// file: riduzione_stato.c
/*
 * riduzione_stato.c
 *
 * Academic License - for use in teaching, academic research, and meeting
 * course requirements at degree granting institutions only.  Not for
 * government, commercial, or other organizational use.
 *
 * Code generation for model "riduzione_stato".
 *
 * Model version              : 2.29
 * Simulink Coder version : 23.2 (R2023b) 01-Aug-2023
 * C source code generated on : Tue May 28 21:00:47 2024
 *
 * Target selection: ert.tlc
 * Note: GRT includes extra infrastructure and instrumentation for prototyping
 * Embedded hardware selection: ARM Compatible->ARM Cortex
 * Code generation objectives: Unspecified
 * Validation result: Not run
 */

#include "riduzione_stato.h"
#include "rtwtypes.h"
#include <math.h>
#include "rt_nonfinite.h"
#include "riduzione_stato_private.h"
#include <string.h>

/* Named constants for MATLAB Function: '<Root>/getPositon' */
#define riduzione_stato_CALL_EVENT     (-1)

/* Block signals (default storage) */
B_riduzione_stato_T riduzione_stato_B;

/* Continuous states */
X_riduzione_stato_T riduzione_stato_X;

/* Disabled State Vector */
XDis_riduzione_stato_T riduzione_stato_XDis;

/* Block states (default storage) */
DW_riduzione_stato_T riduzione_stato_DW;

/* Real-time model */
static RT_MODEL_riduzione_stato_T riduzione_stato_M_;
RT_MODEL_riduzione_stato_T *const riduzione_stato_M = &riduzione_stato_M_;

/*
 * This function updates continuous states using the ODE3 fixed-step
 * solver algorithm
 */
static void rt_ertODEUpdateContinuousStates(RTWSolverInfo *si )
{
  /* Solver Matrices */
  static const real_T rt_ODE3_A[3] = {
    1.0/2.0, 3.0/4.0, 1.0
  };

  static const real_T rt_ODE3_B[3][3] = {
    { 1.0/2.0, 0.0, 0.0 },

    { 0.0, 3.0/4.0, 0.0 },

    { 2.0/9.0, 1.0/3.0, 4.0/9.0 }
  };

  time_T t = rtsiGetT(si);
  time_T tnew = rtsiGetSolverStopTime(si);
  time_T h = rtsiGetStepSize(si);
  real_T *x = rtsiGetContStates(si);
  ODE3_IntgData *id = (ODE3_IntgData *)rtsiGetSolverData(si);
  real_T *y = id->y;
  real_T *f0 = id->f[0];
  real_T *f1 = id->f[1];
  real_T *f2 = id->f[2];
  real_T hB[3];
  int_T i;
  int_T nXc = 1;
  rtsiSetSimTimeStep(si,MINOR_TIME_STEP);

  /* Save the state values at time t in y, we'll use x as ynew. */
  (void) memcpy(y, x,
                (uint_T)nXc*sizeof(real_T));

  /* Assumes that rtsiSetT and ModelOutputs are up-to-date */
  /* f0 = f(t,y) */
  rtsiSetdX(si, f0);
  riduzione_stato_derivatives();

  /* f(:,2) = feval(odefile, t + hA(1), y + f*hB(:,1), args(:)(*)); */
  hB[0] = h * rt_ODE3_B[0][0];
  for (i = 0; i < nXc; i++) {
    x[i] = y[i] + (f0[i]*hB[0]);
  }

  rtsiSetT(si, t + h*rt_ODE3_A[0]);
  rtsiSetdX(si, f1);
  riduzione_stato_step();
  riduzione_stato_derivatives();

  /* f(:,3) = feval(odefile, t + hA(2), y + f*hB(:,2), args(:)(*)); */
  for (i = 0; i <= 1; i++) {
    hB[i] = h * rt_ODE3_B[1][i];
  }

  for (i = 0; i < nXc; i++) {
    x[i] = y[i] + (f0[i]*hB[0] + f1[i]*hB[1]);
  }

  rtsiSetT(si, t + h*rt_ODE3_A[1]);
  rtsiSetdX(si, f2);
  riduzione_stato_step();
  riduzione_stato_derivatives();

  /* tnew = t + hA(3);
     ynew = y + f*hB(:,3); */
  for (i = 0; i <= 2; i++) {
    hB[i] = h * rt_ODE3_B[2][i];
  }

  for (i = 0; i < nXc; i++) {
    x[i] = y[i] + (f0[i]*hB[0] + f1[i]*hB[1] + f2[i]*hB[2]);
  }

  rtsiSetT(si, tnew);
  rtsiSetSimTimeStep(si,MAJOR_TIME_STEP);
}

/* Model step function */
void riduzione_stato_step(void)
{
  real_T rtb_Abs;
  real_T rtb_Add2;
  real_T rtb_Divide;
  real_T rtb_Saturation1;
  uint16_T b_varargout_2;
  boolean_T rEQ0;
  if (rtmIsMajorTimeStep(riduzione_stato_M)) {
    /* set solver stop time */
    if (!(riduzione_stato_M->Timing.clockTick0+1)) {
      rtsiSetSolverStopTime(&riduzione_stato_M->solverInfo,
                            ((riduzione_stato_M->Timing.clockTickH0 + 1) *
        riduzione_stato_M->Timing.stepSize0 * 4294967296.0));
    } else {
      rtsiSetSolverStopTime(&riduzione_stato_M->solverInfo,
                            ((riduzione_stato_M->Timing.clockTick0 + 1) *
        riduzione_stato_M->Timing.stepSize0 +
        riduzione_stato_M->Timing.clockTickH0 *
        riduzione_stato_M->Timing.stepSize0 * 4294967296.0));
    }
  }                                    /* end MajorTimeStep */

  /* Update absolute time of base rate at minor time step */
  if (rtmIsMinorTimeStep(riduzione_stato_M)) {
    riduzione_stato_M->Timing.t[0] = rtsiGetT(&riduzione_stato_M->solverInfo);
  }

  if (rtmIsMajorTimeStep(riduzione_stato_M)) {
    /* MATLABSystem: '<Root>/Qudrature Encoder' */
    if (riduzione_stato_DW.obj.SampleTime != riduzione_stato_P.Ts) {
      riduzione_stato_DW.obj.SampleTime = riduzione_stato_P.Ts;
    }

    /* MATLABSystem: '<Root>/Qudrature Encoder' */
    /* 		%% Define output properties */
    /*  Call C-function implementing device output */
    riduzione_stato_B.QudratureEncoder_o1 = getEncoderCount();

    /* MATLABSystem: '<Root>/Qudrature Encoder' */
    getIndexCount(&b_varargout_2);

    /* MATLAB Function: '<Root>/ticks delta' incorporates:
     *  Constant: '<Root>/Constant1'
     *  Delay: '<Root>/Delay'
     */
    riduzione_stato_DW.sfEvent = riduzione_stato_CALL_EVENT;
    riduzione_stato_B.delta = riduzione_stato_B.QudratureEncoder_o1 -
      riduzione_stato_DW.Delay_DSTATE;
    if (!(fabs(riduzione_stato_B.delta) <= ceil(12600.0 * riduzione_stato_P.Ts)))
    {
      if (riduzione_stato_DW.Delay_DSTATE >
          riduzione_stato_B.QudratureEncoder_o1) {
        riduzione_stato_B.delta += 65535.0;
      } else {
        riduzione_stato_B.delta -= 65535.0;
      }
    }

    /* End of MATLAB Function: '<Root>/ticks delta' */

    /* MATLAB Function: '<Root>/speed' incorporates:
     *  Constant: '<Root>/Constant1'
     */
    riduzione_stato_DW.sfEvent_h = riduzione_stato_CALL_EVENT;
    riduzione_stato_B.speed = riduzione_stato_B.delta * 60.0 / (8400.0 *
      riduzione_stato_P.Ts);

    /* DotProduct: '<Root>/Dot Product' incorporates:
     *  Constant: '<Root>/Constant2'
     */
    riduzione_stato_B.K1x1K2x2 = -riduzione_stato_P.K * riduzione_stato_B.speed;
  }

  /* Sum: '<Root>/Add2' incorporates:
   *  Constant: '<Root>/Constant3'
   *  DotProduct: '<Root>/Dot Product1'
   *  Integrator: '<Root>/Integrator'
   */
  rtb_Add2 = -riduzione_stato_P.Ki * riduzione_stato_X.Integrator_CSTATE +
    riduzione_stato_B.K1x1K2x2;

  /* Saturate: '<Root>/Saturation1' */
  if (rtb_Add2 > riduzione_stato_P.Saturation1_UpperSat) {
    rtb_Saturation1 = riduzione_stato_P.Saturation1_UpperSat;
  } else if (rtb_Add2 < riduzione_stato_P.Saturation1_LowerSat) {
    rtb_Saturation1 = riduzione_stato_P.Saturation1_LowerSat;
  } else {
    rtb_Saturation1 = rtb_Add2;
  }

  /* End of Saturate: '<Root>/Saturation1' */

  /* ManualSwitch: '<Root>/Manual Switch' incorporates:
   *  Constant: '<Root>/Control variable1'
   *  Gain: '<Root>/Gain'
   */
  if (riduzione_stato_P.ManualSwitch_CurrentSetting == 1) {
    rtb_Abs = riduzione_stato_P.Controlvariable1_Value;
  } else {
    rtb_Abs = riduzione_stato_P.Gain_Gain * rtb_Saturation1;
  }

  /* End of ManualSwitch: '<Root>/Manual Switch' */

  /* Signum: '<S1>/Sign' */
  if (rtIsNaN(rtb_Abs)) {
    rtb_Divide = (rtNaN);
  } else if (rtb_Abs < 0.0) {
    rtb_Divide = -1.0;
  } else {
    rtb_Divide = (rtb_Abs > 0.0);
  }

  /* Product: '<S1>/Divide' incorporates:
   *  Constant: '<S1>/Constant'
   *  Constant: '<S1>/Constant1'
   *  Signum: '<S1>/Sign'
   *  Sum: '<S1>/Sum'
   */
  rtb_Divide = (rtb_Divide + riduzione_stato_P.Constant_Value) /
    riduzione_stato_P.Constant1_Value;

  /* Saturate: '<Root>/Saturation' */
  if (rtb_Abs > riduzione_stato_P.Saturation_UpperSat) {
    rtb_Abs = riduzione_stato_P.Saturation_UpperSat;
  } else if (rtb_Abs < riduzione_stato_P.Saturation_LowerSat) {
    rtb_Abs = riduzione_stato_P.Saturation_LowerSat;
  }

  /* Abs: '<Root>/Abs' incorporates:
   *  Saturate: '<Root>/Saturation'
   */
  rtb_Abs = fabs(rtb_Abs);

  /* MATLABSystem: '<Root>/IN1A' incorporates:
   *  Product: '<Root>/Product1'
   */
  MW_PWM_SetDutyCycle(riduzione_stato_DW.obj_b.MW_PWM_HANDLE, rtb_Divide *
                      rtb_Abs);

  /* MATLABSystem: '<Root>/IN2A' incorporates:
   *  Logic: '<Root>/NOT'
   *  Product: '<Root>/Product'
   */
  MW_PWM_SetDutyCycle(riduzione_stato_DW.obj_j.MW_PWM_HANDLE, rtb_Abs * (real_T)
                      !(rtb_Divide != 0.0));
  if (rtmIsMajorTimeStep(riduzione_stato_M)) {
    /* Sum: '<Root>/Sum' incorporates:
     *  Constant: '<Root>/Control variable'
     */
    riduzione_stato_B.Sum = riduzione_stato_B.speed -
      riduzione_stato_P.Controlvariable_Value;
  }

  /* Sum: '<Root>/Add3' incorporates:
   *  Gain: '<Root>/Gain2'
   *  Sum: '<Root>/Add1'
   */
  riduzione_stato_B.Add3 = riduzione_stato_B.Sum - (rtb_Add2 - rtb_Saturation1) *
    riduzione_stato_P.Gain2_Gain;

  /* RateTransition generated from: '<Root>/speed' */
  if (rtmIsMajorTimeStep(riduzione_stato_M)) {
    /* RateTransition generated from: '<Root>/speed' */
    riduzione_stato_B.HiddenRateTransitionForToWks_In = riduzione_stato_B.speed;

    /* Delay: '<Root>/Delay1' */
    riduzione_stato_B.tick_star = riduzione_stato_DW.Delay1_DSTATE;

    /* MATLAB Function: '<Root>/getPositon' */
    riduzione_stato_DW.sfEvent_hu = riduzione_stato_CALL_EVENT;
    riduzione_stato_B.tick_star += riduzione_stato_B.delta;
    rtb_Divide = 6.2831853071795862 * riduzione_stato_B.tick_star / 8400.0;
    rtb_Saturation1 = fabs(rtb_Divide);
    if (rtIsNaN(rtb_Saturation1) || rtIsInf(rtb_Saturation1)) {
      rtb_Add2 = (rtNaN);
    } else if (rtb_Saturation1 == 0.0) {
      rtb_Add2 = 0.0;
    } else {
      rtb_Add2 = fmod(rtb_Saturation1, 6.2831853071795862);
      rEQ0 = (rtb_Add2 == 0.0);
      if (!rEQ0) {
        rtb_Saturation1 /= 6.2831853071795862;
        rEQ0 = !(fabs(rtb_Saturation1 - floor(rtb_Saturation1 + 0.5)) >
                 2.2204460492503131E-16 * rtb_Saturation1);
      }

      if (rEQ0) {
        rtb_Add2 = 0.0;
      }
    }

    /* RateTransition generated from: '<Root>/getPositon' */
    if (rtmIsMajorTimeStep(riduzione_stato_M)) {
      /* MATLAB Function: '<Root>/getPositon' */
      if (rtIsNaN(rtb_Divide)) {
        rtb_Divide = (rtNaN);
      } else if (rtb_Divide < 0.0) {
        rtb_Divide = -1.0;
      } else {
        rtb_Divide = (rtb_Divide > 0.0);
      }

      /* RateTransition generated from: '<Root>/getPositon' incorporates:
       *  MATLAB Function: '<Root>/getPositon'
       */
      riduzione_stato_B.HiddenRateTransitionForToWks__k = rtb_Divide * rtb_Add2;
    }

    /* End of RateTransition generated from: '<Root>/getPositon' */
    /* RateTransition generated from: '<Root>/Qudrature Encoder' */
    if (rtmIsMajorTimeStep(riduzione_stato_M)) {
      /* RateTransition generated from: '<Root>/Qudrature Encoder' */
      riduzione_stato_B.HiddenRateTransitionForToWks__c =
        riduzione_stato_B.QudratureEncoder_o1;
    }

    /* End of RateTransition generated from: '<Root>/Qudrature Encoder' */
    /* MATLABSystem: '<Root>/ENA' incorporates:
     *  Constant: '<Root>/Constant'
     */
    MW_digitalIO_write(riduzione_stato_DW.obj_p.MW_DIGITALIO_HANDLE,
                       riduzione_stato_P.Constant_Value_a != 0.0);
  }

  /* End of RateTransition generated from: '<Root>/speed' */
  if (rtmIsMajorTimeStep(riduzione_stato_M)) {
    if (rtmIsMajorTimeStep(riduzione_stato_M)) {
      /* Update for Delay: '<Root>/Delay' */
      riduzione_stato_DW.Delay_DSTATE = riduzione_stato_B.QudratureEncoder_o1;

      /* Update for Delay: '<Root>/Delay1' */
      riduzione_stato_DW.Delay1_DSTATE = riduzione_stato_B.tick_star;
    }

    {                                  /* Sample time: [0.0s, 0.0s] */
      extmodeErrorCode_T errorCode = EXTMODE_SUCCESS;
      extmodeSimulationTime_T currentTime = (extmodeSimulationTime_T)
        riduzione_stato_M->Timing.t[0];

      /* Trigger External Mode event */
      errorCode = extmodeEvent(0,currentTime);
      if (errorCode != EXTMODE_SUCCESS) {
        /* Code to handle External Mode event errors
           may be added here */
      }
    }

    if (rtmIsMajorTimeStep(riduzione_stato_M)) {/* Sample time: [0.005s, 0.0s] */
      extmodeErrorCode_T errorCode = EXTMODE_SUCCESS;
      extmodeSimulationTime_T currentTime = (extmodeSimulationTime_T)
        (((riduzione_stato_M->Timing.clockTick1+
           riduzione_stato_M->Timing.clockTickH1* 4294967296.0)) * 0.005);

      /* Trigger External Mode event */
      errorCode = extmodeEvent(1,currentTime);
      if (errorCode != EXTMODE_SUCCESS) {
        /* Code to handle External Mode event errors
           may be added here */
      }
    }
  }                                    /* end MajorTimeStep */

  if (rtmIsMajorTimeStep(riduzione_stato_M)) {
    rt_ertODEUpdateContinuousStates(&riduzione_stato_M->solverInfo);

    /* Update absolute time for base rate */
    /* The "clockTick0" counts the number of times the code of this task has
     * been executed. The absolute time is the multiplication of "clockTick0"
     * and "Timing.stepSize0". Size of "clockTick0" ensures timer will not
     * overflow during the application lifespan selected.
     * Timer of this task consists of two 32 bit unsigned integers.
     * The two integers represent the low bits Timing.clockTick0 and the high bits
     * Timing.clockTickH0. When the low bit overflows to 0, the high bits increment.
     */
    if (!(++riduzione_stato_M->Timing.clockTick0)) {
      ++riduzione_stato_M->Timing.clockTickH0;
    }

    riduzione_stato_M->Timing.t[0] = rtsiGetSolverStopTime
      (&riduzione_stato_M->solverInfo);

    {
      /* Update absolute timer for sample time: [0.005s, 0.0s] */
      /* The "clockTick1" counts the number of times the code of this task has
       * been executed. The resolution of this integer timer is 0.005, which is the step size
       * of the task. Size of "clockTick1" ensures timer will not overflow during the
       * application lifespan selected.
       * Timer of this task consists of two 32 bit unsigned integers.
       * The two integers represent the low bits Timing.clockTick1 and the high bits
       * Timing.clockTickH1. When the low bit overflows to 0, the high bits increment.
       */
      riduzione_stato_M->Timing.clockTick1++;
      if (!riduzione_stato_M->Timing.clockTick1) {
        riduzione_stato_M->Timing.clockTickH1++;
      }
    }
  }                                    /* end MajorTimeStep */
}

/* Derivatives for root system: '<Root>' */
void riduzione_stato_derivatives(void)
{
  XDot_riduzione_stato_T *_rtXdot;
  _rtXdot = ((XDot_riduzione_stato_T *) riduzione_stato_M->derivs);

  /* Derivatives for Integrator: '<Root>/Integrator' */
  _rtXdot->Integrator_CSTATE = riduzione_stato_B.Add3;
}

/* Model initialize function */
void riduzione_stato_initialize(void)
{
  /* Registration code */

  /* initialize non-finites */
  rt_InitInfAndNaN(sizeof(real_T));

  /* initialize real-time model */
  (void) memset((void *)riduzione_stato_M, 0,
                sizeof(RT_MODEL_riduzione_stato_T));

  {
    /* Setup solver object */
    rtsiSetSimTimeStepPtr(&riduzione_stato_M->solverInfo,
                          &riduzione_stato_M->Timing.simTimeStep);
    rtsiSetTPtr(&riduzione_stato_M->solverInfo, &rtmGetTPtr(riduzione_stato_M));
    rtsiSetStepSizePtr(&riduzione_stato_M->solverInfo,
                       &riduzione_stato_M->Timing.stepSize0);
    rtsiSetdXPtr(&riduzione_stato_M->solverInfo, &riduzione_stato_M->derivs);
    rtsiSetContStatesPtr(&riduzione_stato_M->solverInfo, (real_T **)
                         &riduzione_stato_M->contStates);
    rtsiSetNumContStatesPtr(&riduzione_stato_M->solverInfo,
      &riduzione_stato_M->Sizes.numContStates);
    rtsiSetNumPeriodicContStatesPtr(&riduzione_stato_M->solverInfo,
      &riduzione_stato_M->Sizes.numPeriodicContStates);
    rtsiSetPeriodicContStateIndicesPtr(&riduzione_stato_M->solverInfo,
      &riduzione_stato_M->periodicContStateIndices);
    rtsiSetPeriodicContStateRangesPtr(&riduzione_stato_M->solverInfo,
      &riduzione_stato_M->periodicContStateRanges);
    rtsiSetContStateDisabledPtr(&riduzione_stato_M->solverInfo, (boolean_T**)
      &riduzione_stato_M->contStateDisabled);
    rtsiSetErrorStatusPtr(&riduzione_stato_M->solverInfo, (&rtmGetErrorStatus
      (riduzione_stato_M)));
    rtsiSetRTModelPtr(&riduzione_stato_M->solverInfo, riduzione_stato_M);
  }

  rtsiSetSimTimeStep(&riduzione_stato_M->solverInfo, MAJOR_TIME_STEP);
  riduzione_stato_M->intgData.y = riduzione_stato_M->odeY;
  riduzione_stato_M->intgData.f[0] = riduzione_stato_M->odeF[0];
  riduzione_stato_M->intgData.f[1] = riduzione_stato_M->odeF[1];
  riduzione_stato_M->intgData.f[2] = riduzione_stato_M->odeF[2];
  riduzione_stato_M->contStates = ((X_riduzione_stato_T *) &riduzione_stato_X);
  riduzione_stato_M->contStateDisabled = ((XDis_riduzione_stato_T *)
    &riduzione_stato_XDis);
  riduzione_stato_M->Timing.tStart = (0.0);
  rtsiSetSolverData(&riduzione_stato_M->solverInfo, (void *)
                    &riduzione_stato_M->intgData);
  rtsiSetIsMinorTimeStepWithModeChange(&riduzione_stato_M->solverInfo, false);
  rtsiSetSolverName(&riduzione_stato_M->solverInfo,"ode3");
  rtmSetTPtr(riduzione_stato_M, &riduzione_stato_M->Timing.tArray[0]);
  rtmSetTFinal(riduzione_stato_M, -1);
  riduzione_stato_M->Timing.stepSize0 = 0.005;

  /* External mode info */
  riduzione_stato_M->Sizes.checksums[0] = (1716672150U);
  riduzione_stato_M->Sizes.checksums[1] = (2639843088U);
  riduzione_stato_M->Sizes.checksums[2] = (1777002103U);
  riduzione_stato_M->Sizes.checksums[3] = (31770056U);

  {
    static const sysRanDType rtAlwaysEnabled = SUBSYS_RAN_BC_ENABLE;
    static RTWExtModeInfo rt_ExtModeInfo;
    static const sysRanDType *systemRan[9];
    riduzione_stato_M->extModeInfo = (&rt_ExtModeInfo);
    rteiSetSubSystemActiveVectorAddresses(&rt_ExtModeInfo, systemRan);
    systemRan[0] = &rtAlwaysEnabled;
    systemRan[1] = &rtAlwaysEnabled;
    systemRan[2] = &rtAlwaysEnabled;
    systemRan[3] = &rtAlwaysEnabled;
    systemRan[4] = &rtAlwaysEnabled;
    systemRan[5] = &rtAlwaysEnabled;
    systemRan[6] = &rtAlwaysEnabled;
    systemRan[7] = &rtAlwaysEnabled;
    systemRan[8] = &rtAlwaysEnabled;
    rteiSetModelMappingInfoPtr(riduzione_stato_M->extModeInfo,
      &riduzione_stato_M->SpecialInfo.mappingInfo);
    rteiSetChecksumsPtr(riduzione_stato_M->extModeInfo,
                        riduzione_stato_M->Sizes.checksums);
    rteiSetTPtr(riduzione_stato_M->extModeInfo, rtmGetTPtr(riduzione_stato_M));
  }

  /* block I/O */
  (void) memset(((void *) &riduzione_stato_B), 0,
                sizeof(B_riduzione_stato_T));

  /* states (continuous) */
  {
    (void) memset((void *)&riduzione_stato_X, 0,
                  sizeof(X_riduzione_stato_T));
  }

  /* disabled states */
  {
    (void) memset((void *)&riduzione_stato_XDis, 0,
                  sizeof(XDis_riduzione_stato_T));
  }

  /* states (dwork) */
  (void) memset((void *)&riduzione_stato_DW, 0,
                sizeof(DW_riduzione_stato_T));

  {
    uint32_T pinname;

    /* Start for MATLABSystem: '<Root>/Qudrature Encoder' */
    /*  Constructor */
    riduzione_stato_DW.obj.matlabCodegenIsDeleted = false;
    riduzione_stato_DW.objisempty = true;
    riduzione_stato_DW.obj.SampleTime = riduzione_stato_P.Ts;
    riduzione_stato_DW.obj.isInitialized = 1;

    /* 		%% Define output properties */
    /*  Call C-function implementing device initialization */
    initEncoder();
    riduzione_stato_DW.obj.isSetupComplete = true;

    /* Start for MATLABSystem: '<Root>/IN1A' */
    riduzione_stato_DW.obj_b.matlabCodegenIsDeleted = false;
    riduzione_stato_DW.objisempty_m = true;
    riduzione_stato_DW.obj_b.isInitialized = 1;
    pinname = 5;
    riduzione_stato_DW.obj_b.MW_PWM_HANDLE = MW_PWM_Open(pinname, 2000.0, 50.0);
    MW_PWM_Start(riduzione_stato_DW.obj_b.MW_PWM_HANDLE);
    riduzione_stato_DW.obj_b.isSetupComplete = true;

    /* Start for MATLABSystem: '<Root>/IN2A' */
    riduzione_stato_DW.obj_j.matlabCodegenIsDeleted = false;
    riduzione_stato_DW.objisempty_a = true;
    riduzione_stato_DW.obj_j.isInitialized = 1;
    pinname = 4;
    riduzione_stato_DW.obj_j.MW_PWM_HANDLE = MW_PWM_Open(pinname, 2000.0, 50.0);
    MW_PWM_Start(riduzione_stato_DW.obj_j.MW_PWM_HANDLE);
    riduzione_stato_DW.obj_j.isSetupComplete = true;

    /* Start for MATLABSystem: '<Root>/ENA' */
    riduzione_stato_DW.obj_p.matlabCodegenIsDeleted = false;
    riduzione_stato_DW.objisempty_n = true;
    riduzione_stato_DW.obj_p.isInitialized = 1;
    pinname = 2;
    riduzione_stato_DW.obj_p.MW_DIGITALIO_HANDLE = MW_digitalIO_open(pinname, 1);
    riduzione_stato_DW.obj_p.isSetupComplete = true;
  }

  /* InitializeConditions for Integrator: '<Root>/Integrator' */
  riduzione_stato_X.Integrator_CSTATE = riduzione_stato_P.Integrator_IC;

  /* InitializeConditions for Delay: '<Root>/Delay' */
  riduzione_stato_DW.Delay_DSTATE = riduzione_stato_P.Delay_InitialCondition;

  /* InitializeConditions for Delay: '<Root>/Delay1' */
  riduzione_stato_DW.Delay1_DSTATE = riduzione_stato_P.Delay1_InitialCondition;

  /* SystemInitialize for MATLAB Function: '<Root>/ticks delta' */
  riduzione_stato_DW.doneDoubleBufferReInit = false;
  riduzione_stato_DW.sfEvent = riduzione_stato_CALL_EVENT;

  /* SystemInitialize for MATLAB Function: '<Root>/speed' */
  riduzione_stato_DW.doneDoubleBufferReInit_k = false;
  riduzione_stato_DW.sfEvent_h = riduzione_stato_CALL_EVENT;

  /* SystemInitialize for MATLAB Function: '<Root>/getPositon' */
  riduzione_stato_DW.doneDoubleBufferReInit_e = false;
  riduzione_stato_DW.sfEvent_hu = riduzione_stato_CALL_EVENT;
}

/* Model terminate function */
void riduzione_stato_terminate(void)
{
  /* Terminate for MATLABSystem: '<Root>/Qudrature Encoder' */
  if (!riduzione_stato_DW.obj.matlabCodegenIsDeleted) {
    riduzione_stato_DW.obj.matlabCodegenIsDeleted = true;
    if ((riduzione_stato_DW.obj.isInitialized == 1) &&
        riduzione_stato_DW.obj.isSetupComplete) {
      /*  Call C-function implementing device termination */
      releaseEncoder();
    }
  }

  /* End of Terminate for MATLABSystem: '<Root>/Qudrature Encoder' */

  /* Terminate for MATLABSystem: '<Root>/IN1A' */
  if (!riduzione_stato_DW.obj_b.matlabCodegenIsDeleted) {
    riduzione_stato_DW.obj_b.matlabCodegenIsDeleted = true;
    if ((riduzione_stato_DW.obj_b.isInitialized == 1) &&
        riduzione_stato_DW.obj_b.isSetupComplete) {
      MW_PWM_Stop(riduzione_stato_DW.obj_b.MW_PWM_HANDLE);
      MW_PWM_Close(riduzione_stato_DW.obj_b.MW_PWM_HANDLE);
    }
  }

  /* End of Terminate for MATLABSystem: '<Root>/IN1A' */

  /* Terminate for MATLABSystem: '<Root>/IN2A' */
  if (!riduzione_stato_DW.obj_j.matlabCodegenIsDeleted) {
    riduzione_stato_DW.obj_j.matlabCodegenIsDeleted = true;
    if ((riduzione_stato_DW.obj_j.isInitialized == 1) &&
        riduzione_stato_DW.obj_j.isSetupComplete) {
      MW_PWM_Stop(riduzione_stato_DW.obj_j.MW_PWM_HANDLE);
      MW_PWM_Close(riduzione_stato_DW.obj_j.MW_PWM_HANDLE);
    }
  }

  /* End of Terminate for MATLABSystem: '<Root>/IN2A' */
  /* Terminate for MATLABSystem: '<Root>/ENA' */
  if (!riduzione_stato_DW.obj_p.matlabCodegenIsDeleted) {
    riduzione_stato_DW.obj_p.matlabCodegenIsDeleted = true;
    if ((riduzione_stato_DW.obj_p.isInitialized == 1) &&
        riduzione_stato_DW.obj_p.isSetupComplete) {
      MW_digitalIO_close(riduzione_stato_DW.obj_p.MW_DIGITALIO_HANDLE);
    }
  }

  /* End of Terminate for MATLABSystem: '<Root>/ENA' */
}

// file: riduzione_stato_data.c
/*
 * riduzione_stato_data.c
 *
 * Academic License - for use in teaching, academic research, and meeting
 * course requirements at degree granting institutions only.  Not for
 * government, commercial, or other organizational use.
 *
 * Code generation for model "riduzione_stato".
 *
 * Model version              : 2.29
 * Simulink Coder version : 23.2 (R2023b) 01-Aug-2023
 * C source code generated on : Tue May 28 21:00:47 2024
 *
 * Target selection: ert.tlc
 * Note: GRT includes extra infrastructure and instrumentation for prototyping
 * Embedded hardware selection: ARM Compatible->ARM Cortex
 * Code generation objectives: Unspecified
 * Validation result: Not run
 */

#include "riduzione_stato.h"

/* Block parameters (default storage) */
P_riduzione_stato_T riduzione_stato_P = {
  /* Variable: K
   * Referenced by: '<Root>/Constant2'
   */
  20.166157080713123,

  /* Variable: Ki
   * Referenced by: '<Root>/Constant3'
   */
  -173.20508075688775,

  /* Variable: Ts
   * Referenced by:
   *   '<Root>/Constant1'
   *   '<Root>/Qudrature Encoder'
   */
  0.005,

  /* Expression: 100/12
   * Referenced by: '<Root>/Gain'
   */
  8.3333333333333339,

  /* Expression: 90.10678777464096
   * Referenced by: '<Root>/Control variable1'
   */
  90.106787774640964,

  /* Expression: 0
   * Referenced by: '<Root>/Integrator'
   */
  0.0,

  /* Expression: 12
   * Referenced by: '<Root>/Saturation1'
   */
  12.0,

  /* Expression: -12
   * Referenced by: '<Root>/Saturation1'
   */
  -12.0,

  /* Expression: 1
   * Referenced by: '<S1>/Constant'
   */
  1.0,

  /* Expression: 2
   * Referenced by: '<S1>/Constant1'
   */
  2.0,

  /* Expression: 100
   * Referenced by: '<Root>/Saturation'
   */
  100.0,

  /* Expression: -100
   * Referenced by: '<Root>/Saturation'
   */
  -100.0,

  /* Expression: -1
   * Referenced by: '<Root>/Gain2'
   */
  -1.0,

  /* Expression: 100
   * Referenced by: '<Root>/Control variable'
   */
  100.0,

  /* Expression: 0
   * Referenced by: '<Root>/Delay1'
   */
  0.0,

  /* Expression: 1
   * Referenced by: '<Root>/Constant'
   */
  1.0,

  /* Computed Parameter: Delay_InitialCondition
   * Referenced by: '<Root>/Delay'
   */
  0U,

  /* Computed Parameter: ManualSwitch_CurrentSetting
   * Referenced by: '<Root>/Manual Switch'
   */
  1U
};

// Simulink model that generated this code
simulink model "riduzione_stato"  (R2023b)
settings: Solver=FixedStepAuto  StartTime=0.0  StopTime=inf  RelTol=1e-3  EnableMultiTasking=on
undefined symbols (not defined in the file): K, Ki, Ts
libraries: mbedblockslib x3, stm_qeplib x1

== system riduzione_stato ==
  Abs : Abs  SaturateOnIntegerOverflow=off
  Add1 : Sum  Inputs=-+
  Add2 : Sum
  Add3 : Sum  Inputs=-+
  Constant : Constant
  Constant1 : Constant  Value=Ts
  Constant2 : Constant  Value=-K
  Constant3 : Constant  Value=-Ki
  Control variable : Constant  Value=-100
  Control variable1 : Constant  Value=100
  Delay : Delay  DelayLength=1
  Delay1 : Delay  DelayLength=1  InitialCondition=0
  Dot Product : DotProduct  OutDataTypeStr=Inherit: Inherit via internal rule
  Dot Product1 : DotProduct  OutDataTypeStr=Inherit: Inherit via internal rule
  ENA : mbedblockslib/Digital Write  Pin=2  Direction=output
  Gain : Gain  Gain=100/12
  Gain2 : Gain  Gain=-1
  IN1A : mbedblockslib/PWM Output  Pin=5  EnableInputFrequency=off  InitialFrequency=2000  InitialDutyCycle=50  NotificationType=None
  IN2A : mbedblockslib/PWM Output  Pin=4  EnableInputFrequency=off  InitialFrequency=2000  InitialDutyCycle=50  NotificationType=None
  Integrator : Integrator
  Manual Switch : ManualSwitch  CurrentSetting=0
  NOT : Logic  Operator=NOT  IconShape=distinctive  AllPortsSameDT=off  OutDataTypeStr=boolean
  Product : Product
  Product1 : Product
  Qudrature Encoder : stm_qeplib/Qudrature Encoder  SampleTime=Ts
  Saturation : Saturate  UpperLimit=100  LowerLimit=-100
  Saturation1 : Saturate  UpperLimit=12  LowerLimit=-12
  Slider : SliderBlock  ScaleMin=-100
  Slider1 : SliderBlock  ScaleMin=-100
  Step : Step  After=50  SampleTime=0
  Subsystem : Subsystem
  Sum : Sum  Inputs=|-+
  getPositon : MATLAB Function  TreatAsAtomicUnit=on
  speed : MATLAB Function  TreatAsAtomicUnit=on
  ticks delta : MATLAB Function  TreatAsAtomicUnit=on
  wires:
  Constant/1 -> ENA/1
  Product/1 -> IN2A/1
  Product1/1 -> IN1A/1
  Saturation/1 -> Abs/1
  Abs/1 -> Product/1, Product1/2
  NOT/1 -> Product/2
  Subsystem/1(Out1) -> Product1/1, NOT/1
  ticks delta/1(delta) -> getPositon/1(delta), speed/1(delta)
  Delay/1 -> ticks delta/2(lastTicks)
  Qudrature Encoder/1 -> ticks delta/1(currentTicks), Delay/1
  Constant1/1 -> ticks delta/3(Ts), speed/2(Ts)
  getPositon/2(tick_star) -> Delay1/1
  Delay1/1 -> getPositon/2("tick_star ")
  Control variable/1 -> Sum/1
  Constant3/1 -> Dot Product1/1  "Ki"
  Dot Product1/1 -> Add2/1  "Ki*z"
  Dot Product/1 -> Add2/2  "-K1*x1-K2*x2"
  Constant2/1 -> Dot Product/1  "-K"
  speed/1(speed) -> Sum/2, Dot Product/2  "speed"
  Manual Switch/1 -> Saturation/1, Subsystem/1(In1)
  Control variable1/1 -> Manual Switch/1
  Add2/1 -> Add1/2, Saturation1/1
  Saturation1/1 -> Gain/1, Add1/1
  Gain/1 -> Manual Switch/2
  Add1/1 -> Gain2/1
  Gain2/1 -> Add3/1
  Sum/1 -> Integrator/1
  Integrator/1 -> Add3/2
  Add3/1 -> Dot Product1/2

== system riduzione_stato/Subsystem ==
  In1 : Inport
  Constant : Constant
  Constant1 : Constant  Value=2
  Divide : Product  Inputs=*/
  Sign : Signum
  Sum : Sum  Inputs=|++
  Out1 : Outport
  wires:
  In1/1 -> Sign/1
  Sign/1 -> Sum/1
  Constant/1 -> Sum/2
  Sum/1 -> Divide/1
  Divide/1 -> Out1/1
  Constant1/1 -> Divide/2

== matlab function riduzione_stato/ticks delta ==
function delta = getTicksData(currentTicks, lastTicks, Ts)

currentTicks = double(currentTicks);
lastTicks = double(lastTicks);

if abs(currentTicks - lastTicks) <= ceil(12600*Ts)
    delta = currentTicks - lastTicks;
else
    if lastTicks > currentTicks
        delta = currentTicks + 2^16-1 - lastTicks;
    else
        delta = currentTicks - 2^16+1 - lastTicks;
    end
end

end

== matlab function riduzione_stato/getPositon ==
function [position, tick_star] = getPosition(delta, tick_star)

tick_star = double(tick_star + delta);

completeTheta = 2 * pi * tick_star /(8400);

position = sign(completeTheta) * mod(abs(completeTheta), 2*pi);

end

== matlab function riduzione_stato/speed ==
function speed = getSpeedByDelta(delta, Ts)

speed = delta * 60 / (8400*Ts);

end
